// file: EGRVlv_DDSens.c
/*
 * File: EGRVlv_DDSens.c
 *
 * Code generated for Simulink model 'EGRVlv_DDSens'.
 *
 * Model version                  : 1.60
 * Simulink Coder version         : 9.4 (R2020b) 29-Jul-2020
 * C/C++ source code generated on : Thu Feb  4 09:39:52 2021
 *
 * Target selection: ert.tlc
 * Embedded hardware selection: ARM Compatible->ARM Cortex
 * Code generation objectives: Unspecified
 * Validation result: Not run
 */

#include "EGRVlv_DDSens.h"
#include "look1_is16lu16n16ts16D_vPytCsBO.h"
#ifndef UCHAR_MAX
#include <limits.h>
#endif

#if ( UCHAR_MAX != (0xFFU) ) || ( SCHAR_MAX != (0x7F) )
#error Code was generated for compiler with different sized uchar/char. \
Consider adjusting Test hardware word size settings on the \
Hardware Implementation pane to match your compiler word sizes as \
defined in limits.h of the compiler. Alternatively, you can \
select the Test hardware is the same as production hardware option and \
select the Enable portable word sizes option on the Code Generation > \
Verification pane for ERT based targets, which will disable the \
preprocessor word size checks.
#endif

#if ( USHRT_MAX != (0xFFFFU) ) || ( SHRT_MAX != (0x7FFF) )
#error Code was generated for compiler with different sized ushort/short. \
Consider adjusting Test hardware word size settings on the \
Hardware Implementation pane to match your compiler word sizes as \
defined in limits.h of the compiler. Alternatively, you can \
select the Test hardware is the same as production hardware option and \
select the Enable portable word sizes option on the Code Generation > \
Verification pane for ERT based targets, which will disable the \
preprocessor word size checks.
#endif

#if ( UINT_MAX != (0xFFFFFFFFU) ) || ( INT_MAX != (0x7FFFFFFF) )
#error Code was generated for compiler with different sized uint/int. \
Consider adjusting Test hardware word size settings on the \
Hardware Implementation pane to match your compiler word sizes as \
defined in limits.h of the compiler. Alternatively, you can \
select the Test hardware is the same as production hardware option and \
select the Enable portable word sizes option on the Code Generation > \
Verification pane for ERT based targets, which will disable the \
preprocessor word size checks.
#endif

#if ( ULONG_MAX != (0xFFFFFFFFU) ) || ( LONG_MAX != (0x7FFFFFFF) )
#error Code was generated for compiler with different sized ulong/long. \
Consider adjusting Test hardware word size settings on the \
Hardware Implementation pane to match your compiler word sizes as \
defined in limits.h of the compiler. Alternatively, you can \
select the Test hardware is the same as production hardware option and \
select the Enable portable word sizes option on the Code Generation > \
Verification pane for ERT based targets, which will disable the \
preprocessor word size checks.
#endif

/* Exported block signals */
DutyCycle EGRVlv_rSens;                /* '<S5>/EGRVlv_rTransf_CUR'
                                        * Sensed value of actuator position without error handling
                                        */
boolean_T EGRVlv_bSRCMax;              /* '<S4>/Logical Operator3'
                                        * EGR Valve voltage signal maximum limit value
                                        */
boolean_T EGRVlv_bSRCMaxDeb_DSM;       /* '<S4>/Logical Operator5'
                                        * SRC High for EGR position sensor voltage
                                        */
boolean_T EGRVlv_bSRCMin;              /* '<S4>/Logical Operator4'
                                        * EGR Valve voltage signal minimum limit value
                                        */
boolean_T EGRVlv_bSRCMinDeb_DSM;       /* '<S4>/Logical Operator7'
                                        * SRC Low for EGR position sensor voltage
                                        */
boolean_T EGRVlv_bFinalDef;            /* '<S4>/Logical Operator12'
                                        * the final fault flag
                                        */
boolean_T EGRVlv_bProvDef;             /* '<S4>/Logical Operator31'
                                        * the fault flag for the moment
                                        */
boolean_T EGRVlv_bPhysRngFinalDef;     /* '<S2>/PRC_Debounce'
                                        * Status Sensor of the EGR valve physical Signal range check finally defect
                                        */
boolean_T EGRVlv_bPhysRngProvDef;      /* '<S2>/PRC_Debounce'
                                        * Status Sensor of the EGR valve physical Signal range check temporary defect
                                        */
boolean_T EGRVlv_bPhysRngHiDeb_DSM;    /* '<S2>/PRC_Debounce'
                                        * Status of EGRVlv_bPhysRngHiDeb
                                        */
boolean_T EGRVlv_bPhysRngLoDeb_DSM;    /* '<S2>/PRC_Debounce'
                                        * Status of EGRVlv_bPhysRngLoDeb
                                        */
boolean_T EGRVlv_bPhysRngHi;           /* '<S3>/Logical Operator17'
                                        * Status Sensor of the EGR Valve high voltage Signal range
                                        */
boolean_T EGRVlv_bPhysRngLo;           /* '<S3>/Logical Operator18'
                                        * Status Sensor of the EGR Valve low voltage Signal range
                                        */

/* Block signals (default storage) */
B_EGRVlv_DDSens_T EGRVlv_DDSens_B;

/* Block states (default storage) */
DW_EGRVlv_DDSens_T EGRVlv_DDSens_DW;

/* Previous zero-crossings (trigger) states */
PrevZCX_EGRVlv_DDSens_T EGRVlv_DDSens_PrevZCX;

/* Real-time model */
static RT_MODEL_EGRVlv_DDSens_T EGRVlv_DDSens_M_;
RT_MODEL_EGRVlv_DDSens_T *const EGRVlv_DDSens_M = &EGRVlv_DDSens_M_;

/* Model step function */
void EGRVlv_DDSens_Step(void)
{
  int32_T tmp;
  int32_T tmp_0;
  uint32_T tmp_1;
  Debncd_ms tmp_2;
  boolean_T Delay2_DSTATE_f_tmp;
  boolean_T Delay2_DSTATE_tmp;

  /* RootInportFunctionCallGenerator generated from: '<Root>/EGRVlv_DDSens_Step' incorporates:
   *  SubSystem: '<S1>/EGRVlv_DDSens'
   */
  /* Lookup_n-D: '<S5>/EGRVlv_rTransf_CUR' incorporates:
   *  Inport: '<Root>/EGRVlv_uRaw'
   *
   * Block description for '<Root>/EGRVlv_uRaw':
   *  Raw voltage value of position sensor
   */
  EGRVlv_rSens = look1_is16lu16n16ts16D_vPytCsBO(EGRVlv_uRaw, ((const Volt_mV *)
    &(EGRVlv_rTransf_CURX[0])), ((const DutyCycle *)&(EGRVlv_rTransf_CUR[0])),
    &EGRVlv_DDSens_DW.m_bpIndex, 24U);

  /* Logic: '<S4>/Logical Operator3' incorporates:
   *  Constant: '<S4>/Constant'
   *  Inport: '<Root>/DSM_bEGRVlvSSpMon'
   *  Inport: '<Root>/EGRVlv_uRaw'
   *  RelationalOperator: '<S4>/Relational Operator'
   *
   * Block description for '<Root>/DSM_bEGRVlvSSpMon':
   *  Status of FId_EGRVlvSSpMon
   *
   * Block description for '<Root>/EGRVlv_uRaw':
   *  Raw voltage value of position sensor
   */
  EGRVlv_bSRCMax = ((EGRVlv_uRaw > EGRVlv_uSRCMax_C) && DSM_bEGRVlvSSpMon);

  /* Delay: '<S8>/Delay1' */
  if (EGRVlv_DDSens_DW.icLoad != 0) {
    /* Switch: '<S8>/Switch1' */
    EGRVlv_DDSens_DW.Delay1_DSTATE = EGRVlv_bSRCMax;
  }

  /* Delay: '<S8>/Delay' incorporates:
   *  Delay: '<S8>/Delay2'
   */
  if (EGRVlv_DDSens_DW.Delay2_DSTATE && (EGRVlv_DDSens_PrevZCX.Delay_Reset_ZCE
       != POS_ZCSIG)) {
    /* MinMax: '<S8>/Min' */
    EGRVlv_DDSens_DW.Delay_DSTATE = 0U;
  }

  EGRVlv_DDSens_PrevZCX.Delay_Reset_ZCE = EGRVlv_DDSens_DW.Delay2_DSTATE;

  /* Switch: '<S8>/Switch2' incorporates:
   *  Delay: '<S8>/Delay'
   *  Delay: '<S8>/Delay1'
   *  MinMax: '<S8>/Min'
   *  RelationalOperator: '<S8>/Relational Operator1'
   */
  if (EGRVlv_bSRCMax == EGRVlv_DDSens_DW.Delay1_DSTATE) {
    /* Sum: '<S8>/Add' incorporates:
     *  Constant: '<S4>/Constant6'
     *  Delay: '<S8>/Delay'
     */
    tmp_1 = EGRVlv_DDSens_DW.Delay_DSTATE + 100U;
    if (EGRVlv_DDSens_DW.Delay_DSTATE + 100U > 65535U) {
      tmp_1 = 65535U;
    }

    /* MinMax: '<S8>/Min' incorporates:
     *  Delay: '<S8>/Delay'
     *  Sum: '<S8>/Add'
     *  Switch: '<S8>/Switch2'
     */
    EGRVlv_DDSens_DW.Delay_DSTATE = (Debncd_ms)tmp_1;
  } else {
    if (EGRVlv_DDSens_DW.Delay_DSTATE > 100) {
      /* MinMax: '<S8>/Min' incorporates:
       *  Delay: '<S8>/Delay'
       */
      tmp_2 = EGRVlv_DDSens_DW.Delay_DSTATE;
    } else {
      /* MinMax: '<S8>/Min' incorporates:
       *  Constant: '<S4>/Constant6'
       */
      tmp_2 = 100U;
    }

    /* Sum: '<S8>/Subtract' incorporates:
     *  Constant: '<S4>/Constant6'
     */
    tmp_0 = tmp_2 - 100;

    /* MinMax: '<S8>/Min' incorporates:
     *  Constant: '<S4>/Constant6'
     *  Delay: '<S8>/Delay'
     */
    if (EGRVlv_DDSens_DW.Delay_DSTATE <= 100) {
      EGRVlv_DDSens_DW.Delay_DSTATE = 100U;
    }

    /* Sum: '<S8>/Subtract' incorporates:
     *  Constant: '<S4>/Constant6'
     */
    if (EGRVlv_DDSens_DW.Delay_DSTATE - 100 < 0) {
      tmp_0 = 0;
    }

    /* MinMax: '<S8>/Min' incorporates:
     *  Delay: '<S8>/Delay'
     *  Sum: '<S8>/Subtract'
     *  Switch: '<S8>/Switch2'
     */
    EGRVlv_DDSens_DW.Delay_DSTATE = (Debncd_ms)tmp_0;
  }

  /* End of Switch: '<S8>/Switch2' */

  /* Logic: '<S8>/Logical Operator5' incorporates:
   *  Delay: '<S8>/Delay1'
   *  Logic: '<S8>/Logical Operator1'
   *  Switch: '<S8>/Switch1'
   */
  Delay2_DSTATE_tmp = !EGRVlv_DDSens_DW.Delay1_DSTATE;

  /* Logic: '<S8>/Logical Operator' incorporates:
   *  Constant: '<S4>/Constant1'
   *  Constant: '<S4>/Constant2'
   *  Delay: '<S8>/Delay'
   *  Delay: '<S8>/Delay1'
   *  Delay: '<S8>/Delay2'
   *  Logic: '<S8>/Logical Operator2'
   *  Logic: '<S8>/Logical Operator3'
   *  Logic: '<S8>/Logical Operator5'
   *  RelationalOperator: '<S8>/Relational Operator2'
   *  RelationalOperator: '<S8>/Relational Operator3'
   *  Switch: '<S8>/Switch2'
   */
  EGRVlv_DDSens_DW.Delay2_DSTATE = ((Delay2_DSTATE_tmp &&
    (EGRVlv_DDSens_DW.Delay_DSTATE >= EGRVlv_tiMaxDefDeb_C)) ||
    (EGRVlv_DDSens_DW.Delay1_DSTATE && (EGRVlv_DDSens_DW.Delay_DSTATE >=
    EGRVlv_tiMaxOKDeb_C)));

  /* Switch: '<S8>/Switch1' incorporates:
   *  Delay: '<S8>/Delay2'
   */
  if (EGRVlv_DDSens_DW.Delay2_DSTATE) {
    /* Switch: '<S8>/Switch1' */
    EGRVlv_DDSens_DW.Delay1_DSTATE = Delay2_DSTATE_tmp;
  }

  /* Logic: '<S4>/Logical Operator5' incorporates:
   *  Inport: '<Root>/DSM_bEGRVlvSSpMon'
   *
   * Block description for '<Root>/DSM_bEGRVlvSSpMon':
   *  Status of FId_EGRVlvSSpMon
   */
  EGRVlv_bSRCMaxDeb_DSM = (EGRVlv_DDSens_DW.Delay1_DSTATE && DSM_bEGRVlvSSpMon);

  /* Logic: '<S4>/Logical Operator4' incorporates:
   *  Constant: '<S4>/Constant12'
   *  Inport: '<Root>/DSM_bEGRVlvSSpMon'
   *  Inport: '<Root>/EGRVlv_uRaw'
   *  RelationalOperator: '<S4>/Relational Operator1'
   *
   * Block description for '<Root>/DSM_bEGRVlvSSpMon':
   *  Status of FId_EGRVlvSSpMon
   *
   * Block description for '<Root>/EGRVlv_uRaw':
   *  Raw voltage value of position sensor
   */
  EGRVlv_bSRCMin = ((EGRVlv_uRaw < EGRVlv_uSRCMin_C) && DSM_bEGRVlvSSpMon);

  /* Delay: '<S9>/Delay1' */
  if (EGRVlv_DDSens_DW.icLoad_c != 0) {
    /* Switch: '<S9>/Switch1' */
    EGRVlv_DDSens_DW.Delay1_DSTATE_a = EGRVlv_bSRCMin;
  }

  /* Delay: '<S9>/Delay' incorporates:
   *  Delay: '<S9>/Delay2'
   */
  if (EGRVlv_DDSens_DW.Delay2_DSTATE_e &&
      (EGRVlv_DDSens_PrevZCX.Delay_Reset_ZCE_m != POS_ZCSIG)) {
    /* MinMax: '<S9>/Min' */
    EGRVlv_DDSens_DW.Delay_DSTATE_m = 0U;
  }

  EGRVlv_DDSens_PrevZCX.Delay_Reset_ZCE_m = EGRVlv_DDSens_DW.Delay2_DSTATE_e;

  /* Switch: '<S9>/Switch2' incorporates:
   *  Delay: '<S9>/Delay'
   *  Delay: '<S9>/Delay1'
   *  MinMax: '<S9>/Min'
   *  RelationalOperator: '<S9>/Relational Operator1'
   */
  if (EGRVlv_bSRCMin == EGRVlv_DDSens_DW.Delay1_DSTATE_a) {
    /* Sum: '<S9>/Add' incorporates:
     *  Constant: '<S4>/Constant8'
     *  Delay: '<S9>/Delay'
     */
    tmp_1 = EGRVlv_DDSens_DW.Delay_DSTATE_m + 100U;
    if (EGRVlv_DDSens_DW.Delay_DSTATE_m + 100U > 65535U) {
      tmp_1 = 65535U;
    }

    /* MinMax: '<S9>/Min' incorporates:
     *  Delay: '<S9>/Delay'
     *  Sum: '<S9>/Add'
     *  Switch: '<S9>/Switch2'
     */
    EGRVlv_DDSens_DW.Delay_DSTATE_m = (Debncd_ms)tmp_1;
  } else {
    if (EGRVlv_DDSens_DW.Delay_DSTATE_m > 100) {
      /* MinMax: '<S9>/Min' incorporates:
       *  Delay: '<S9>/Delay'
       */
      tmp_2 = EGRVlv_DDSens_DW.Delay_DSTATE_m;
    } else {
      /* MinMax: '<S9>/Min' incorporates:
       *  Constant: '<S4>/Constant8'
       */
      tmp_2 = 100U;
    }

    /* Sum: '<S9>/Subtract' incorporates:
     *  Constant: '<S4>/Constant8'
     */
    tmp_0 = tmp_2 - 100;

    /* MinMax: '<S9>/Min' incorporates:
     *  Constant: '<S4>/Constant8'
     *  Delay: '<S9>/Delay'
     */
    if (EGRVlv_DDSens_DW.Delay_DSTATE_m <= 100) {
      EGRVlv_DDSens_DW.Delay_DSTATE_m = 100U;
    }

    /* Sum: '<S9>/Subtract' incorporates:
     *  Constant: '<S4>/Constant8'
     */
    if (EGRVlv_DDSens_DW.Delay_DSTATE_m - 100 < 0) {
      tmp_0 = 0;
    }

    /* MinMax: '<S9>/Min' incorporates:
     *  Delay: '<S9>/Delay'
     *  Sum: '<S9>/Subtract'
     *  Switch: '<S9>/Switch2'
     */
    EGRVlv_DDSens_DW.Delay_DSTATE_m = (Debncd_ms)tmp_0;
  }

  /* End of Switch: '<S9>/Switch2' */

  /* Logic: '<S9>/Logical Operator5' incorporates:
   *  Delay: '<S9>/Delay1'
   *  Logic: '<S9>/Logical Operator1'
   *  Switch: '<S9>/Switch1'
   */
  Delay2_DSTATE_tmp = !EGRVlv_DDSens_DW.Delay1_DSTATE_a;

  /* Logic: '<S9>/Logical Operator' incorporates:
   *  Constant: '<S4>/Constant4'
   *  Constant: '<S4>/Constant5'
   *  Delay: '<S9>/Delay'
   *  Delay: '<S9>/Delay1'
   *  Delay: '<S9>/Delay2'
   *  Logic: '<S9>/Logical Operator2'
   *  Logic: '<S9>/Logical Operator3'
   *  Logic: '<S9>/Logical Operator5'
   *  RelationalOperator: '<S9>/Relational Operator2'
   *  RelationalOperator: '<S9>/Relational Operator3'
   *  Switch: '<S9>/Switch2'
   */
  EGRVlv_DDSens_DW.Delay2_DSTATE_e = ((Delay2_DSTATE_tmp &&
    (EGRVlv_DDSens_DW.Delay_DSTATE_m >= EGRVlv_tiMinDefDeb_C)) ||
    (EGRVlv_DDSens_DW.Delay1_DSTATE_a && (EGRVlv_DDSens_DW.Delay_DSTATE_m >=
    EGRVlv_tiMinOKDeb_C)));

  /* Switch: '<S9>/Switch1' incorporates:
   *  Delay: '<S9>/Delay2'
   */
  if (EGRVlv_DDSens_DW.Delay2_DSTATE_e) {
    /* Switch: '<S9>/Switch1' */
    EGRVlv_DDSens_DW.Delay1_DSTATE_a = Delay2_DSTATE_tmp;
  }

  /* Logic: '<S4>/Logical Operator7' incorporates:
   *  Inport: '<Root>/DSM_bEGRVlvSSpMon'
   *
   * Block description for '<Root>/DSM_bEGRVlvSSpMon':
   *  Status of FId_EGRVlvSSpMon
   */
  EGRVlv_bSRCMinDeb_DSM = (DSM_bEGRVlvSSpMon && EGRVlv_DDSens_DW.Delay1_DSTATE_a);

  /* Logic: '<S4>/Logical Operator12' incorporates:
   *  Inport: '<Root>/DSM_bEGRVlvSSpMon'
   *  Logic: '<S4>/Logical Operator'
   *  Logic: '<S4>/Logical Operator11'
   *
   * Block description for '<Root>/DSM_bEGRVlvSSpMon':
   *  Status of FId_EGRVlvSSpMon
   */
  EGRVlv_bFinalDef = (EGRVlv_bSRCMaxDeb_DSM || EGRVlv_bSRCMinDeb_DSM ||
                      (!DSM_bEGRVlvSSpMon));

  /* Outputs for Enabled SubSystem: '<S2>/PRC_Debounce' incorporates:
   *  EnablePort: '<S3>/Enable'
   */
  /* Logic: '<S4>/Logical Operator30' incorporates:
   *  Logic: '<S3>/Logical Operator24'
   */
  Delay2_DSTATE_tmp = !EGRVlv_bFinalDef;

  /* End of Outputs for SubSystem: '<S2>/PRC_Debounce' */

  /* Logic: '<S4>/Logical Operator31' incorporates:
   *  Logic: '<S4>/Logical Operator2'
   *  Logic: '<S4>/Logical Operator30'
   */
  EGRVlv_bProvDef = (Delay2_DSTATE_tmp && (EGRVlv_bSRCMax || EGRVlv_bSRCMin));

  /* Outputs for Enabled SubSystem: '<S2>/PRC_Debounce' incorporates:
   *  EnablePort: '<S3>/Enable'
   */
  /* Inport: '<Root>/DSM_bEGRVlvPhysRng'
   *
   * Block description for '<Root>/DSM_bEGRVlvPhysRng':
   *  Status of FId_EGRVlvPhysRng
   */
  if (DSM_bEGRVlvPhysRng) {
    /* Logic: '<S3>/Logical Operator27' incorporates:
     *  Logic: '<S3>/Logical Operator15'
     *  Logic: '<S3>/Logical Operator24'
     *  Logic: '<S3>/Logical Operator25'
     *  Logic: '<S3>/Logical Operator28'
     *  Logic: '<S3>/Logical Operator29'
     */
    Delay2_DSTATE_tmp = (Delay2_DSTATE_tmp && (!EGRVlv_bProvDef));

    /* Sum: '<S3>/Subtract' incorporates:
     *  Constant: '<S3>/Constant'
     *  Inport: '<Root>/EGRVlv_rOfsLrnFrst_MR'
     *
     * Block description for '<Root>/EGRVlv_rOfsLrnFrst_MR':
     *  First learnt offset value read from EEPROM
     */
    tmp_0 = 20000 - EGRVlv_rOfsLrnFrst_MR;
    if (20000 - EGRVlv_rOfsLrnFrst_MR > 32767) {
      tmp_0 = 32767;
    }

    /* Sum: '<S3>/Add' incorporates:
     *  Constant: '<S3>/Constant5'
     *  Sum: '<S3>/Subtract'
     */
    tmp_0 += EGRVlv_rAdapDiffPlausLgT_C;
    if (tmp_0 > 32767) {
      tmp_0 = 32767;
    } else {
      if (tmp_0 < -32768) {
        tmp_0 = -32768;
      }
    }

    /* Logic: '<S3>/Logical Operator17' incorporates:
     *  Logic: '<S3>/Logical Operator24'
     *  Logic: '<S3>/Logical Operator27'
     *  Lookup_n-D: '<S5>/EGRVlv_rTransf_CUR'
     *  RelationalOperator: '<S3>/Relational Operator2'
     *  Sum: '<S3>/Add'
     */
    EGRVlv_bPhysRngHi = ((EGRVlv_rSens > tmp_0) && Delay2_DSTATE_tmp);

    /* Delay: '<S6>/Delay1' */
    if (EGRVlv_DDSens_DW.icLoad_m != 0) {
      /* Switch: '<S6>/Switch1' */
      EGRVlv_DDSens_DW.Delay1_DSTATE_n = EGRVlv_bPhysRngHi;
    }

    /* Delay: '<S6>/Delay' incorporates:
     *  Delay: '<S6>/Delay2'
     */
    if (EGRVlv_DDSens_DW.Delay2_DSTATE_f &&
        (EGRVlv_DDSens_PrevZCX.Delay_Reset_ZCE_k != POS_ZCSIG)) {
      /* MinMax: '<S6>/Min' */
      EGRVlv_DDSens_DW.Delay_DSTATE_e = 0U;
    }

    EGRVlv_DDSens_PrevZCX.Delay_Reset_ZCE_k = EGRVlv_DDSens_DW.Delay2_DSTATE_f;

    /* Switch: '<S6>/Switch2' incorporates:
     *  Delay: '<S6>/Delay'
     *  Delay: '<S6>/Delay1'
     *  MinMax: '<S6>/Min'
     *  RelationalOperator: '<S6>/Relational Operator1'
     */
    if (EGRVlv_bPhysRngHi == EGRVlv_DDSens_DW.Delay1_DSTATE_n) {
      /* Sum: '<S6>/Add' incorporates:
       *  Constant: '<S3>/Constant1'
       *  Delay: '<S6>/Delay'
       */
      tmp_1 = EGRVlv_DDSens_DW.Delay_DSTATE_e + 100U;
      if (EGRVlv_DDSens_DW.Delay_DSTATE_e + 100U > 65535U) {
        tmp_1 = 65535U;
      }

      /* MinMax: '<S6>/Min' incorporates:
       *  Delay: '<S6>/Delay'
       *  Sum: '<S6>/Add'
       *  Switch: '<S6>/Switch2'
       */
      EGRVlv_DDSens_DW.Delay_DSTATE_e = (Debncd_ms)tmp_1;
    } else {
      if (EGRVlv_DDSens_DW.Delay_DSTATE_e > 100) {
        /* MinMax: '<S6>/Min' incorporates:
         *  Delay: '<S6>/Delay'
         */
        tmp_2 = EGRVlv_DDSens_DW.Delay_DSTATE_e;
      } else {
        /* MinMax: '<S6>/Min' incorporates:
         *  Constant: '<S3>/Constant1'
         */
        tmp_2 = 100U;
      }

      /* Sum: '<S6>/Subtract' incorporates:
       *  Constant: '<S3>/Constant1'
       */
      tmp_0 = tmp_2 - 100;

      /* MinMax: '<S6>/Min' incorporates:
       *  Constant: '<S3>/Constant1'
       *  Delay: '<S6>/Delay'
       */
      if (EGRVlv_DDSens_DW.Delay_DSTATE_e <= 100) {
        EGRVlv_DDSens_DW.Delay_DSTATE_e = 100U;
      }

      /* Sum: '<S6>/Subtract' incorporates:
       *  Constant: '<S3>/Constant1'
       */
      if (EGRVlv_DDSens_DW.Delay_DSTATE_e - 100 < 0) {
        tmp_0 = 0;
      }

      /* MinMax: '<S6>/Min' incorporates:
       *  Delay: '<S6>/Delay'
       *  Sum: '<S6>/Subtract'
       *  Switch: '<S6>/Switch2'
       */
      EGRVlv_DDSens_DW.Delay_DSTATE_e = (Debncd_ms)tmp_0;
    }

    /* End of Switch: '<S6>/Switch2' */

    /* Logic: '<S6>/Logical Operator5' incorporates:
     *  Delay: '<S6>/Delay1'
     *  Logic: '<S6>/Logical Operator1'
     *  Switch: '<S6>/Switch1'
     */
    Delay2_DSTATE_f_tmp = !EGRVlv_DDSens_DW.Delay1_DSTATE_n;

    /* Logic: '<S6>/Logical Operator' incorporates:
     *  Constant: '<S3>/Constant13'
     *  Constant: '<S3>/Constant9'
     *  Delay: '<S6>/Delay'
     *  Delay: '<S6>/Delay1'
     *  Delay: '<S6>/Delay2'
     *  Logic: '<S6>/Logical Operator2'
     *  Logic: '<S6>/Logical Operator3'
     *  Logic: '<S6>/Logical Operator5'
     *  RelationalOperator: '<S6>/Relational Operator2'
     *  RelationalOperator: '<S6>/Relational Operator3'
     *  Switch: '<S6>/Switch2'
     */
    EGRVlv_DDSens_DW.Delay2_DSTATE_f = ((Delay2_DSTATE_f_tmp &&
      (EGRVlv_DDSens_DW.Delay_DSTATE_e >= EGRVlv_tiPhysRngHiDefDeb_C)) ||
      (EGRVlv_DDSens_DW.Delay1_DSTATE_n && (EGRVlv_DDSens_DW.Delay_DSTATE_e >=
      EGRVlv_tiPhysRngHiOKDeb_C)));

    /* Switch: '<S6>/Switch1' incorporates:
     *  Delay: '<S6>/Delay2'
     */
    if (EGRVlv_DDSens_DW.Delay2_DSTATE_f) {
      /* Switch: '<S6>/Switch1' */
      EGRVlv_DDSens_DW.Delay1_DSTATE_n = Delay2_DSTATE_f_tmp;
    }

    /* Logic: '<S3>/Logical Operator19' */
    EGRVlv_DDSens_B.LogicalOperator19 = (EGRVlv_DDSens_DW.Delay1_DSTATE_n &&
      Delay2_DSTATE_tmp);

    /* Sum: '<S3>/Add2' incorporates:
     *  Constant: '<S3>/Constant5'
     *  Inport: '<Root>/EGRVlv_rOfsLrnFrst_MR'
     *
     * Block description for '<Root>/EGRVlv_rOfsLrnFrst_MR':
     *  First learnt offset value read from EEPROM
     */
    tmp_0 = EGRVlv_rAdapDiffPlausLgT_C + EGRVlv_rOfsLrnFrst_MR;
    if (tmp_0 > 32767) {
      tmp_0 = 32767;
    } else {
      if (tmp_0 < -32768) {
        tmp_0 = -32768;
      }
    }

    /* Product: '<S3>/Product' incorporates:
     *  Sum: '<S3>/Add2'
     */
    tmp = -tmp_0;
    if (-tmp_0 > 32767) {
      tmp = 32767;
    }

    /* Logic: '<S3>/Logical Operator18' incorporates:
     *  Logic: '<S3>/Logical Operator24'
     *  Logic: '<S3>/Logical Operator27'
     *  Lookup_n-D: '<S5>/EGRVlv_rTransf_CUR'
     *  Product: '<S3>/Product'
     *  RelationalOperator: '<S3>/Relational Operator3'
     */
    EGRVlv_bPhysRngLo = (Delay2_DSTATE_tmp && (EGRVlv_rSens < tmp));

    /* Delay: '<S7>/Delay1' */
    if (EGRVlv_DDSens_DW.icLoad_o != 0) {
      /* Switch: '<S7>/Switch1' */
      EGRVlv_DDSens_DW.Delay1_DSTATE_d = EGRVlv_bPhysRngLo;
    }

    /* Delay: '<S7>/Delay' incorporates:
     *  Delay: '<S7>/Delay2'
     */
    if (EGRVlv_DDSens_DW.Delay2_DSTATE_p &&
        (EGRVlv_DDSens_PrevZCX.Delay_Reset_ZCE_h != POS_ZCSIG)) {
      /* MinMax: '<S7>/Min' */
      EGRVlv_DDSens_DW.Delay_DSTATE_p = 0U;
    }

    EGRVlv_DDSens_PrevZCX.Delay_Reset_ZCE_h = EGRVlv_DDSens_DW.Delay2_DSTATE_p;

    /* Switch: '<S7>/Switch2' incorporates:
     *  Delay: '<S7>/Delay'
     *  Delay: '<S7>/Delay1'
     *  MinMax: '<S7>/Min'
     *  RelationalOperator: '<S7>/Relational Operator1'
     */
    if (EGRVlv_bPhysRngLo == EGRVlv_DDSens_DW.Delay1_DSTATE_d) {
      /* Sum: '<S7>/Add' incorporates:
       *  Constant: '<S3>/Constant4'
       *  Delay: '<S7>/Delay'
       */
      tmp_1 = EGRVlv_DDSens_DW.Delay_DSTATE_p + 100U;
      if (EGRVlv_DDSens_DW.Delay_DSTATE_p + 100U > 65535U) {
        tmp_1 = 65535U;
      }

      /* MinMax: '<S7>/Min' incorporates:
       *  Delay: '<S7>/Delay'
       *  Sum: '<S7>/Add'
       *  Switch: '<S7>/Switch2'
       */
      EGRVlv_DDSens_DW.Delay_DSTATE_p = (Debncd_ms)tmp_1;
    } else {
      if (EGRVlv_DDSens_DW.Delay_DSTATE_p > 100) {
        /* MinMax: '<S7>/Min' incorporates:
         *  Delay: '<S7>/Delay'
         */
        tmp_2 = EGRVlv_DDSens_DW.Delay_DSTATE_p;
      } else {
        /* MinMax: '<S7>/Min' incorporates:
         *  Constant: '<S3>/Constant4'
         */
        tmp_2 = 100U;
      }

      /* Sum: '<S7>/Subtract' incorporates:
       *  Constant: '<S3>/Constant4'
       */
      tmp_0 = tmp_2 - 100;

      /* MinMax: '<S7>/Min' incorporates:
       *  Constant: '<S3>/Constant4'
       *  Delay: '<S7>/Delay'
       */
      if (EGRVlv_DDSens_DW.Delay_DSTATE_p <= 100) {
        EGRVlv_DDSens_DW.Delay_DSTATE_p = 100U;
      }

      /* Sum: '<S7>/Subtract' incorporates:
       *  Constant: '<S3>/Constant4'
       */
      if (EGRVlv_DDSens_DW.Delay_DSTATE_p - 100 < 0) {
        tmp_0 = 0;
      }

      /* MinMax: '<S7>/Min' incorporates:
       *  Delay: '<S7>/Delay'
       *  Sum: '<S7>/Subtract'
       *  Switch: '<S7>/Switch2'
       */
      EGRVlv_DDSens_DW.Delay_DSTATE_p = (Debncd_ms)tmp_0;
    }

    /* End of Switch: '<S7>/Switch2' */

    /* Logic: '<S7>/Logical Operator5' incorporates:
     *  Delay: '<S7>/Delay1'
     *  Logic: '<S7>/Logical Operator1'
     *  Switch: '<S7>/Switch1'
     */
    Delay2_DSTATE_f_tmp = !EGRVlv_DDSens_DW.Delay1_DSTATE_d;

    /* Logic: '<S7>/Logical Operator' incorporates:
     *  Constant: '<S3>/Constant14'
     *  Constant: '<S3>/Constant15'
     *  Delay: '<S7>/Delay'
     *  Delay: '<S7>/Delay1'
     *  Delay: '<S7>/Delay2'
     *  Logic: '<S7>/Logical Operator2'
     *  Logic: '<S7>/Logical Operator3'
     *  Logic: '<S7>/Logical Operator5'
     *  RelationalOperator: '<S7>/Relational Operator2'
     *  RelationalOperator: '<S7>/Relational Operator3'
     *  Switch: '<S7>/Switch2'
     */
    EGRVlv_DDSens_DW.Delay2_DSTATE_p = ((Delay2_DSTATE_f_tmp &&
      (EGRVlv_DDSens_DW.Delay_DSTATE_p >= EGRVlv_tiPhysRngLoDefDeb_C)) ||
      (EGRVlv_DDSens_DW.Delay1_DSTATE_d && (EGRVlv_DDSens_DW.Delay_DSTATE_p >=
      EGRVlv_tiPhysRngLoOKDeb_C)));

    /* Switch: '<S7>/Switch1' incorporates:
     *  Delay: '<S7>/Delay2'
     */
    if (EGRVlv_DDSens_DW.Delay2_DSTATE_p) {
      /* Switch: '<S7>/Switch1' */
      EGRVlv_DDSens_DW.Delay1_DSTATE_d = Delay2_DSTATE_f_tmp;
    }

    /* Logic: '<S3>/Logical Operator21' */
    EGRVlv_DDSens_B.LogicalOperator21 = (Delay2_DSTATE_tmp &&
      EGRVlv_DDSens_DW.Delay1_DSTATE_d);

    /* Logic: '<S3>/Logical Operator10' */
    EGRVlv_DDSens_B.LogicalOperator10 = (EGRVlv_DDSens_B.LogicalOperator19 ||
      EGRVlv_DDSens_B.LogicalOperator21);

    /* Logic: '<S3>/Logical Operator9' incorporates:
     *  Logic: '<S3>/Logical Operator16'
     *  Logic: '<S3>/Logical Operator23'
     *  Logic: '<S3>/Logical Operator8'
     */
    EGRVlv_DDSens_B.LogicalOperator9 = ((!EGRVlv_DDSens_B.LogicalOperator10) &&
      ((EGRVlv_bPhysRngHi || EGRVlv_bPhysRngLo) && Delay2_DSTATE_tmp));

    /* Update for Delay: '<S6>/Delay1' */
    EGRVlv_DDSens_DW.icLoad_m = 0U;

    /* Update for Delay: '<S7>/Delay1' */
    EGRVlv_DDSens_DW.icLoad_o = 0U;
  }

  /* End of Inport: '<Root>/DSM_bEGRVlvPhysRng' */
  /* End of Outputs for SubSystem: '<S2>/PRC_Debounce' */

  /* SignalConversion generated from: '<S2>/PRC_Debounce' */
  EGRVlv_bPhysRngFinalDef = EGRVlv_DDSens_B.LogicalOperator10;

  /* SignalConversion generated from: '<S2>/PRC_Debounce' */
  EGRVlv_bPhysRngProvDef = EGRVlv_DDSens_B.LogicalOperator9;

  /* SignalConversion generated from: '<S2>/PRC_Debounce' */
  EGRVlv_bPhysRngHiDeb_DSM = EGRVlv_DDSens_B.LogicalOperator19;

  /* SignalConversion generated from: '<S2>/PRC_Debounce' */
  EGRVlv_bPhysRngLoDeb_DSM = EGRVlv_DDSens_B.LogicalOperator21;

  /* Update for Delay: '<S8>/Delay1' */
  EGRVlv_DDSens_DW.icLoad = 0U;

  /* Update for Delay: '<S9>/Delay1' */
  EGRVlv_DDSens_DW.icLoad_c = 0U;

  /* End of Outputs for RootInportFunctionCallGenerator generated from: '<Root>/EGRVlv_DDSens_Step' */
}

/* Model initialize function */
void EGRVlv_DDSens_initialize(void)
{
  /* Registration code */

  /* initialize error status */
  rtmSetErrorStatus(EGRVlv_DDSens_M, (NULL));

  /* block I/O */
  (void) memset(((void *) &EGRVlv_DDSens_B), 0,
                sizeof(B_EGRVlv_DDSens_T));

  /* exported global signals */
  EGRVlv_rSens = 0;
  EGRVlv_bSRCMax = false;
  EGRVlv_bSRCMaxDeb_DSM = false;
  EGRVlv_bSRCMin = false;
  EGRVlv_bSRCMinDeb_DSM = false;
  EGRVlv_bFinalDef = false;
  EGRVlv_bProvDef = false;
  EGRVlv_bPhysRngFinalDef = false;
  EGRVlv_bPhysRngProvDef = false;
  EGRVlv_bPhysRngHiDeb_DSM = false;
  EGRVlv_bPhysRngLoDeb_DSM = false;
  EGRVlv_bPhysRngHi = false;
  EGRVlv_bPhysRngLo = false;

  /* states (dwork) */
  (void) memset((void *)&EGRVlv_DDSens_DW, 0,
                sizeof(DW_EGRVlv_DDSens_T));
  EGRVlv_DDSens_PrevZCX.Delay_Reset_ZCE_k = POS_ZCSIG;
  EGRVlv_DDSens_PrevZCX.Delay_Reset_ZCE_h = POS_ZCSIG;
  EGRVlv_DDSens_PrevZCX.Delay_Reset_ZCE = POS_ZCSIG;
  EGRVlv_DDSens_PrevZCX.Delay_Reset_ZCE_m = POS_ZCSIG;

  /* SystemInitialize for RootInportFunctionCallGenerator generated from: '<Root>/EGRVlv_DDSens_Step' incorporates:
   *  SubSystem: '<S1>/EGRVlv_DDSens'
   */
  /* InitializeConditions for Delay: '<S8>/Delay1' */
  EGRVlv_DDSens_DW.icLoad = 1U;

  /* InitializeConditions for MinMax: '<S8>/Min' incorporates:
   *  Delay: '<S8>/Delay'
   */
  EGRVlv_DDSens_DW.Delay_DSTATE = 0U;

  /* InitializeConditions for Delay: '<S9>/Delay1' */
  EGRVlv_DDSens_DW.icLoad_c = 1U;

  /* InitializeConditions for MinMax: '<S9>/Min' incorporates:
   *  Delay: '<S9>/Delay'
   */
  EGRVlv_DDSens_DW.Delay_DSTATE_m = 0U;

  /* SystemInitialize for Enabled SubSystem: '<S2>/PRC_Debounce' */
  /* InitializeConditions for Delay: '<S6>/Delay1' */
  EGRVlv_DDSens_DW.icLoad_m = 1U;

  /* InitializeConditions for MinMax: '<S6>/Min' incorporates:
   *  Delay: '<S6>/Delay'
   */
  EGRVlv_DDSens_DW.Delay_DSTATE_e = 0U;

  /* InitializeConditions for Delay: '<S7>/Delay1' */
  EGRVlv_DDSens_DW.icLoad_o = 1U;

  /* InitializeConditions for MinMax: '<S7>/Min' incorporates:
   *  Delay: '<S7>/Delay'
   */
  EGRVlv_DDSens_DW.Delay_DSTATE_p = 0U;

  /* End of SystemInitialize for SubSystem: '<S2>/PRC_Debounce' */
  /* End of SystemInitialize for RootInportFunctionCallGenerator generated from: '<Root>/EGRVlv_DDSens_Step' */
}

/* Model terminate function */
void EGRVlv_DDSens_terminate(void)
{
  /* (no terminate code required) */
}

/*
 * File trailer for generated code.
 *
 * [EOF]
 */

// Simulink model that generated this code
simulink model "EGRVlv_DDSens"  (R2018a)
settings: configuration reference "cs_ert" (kept outside this file)
model workspace (MAT data in the model file):
  EGRVlv_DDSens_DT = 10
values from neighbouring files (symbols this model uses):
  EGRVlv_rAdapDiffPlausLgT_C = 20.0    [EGRVlv_DDSens.sldd]
  EGRVlv_rTransf_CUR : value not decoded    [EGRVlv_DDSens.sldd]
  EGRVlv_rTransf_CURX : value not decoded    [EGRVlv_DDSens.sldd]
  EGRVlv_tiMaxDefDeb_C = 200.0    [EGRVlv_DDSens.sldd]
  EGRVlv_tiMaxOKDeb_C = 200.0    [EGRVlv_DDSens.sldd]
  EGRVlv_tiMinDefDeb_C = 200.0    [EGRVlv_DDSens.sldd]
  EGRVlv_tiMinOKDeb_C = 200.0    [EGRVlv_DDSens.sldd]
  EGRVlv_tiPhysRngHiDefDeb_C = 200.0    [EGRVlv_DDSens.sldd]
  EGRVlv_tiPhysRngHiOKDeb_C = 200.0    [EGRVlv_DDSens.sldd]
  EGRVlv_tiPhysRngLoDefDeb_C = 200.0    [EGRVlv_DDSens.sldd]
  EGRVlv_tiPhysRngLoOKDeb_C = 200.0    [EGRVlv_DDSens.sldd]
  EGRVlv_uSRCMax_C = 4800.0    [EGRVlv_DDSens.sldd]
  EGRVlv_uSRCMin_C = 200.0    [EGRVlv_DDSens.sldd]
undefined symbols (not defined in the file or in its folder): CEngDsT_tTransf_CURX
libraries: sllib x4

== system EGRVlv_DDSens ==
  EGRVlv_DDSens_Step : Inport  OutputFunctionCall=on
  EGRVlv_uRaw : Inport  Description=Raw voltage value of position sensor  Port=2  OutMin=0  OutMax=5000  OutDataTypeStr=Volt_mV  Unit=mv  PortDimensions=[1 1]
  DSM_bEGRVlvSSpMon : Inport  Description=Status of FId_EGRVlvSSpMon  Port=3  OutMin=0  OutMax=1  OutDataTypeStr=boolean  PortDimensions=[1 1]
  EGRVlv_rOfsLrnFrst_MR : Inport  Description=First learnt offset value read from EEPROM  Port=4  OutMin=-100  OutMax=100  OutDataTypeStr=DutyCycle  Unit=%  PortDimensions=[1 1]
  DSM_bEGRVlvPhysRng : Inport  Description=Status of FId_EGRVlvPhysRng  Port=5  OutMin=0  OutMax=1  OutDataTypeStr=boolean  PortDimensions=[1 1]
  Overview : Subsystem
  EGRVlv_rSens : Outport  Description=Sensed value of actuator position without error handling  OutMin=-100  OutMax=100  OutDataTypeStr=DutyCycle  Unit=%  PortDimensions=[1 1]
  EGRVlv_bFinalDef : Outport  Description=the final fault flag  Port=2  OutMin=0  OutMax=1  OutDataTypeStr=boolean  PortDimensions=[1 1]
  EGRVlv_bProvDef : Outport  Description=the fault flag for the moment  Port=3  OutMin=0  OutMax=1  OutDataTypeStr=boolean  PortDimensions=[1 1]
  EGRVlv_bSRCMaxDeb_DSM : Outport  Description=SRC High for EGR position sensor voltage  Port=4  OutMin=0  OutMax=1  OutDataTypeStr=boolean  PortDimensions=[1 1]
  EGRVlv_bSRCMinDeb_DSM : Outport  Description=SRC Low for EGR position sensor voltage  Port=5  OutMin=0  OutMax=1  OutDataTypeStr=boolean  PortDimensions=[1 1]
  EGRVlv_bPhysRngHiDeb_DSM : Outport  Description=Status of EGRVlv_bPhysRngHiDeb  Port=6  OutMin=0  OutMax=1  OutDataTypeStr=boolean  PortDimensions=[1 1]
  EGRVlv_bPhysRngLoDeb_DSM : Outport  Description=Status of EGRVlv_bPhysRngLoDeb  Port=7  OutMin=0  OutMax=1  OutDataTypeStr=boolean  PortDimensions=[1 1]
  EGRVlv_bPhysRngFinalDef : Outport  Description=Status Sensor of the EGR valve physical Signal range check finally defect  Port=8  OutMin=0  OutMax=1  OutDataTypeStr=boolean  PortDimensions=[1 1]
  EGRVlv_bPhysRngProvDef : Outport  Description=Status Sensor of the EGR valve physical Signal range check temporary defect  Port=9  OutMin=0  OutMax=1  OutDataTypeStr=boolean  PortDimensions=[1 1]
  wires:
  EGRVlv_DDSens_Step/1 -> Overview/1(EGRVlv_DDSens_Step)
  EGRVlv_uRaw/1 -> Overview/2(EGRVlv_uRaw)
  DSM_bEGRVlvSSpMon/1 -> Overview/3(DSM_bEGRVlvSSpMon)
  EGRVlv_rOfsLrnFrst_MR/1 -> Overview/4(EGRVlv_rOfsLrnFrst_MR)
  DSM_bEGRVlvPhysRng/1 -> Overview/5(DSM_bEGRVlvPhysRng)
  Overview/1(EGRVlv_rSens) -> EGRVlv_rSens/1
  Overview/2(EGRVlv_bFinalDef) -> EGRVlv_bFinalDef/1
  Overview/3(EGRVlv_bProvDef) -> EGRVlv_bProvDef/1
  Overview/4(EGRVlv_bSRCMaxDeb_DSM) -> EGRVlv_bSRCMaxDeb_DSM/1
  Overview/5(EGRVlv_bSRCMinDeb_DSM) -> EGRVlv_bSRCMinDeb_DSM/1
  Overview/6(EGRVlv_bPhysRngHiDeb_DSM) -> EGRVlv_bPhysRngHiDeb_DSM/1
  Overview/7(EGRVlv_bPhysRngLoDeb_DSM) -> EGRVlv_bPhysRngLoDeb_DSM/1
  Overview/8(EGRVlv_bPhysRngFinalDef) -> EGRVlv_bPhysRngFinalDef/1
  Overview/9(EGRVlv_bPhysRngProvDef) -> EGRVlv_bPhysRngProvDef/1

== system EGRVlv_DDSens/Overview ==
  EGRVlv_DDSens_Step : Inport
  EGRVlv_uRaw : Inport  Port=2
  DSM_bEGRVlvSSpMon : Inport  Port=3
  EGRVlv_rOfsLrnFrst_MR : Inport  Port=4
  DSM_bEGRVlvPhysRng : Inport  Port=5
  EGRVlv_DDSens : Subsystem
  EGRVlv_rSens : Outport
  EGRVlv_bFinalDef : Outport  Port=2
  EGRVlv_bProvDef : Outport  Port=3
  EGRVlv_bSRCMaxDeb_DSM : Outport  Port=4
  EGRVlv_bSRCMinDeb_DSM : Outport  Port=5
  EGRVlv_bPhysRngHiDeb_DSM : Outport  Port=6
  EGRVlv_bPhysRngLoDeb_DSM : Outport  Port=7
  EGRVlv_bPhysRngFinalDef : Outport  Port=8
  EGRVlv_bPhysRngProvDef : Outport  Port=9
  wires:
  EGRVlv_uRaw/1 -> EGRVlv_DDSens/1(EGRVlv_uRaw)
  DSM_bEGRVlvSSpMon/1 -> EGRVlv_DDSens/2(DSM_bEGRVlvSSpMon)
  EGRVlv_rOfsLrnFrst_MR/1 -> EGRVlv_DDSens/3(EGRVlv_rOfsLrnFrst_MR)
  DSM_bEGRVlvPhysRng/1 -> EGRVlv_DDSens/4(DSM_bEGRVlvPhysRng)
  EGRVlv_DDSens/1(EGRVlv_rSens) -> EGRVlv_rSens/1
  EGRVlv_DDSens/2(EGRVlv_bFinalDef) -> EGRVlv_bFinalDef/1
  EGRVlv_DDSens/3(EGRVlv_bProvDef) -> EGRVlv_bProvDef/1
  EGRVlv_DDSens/4(EGRVlv_bSRCMaxDeb_DSM) -> EGRVlv_bSRCMaxDeb_DSM/1
  EGRVlv_DDSens/5(EGRVlv_bSRCMinDeb_DSM) -> EGRVlv_bSRCMinDeb_DSM/1
  EGRVlv_DDSens/6(EGRVlv_bPhysRngHiDeb_DSM) -> EGRVlv_bPhysRngHiDeb_DSM/1
  EGRVlv_DDSens/7(EGRVlv_bPhysRngLoDeb_DSM) -> EGRVlv_bPhysRngLoDeb_DSM/1
  EGRVlv_DDSens/8(EGRVlv_bPhysRngFinalDef) -> EGRVlv_bPhysRngFinalDef/1
  EGRVlv_DDSens/9(EGRVlv_bPhysRngProvDef) -> EGRVlv_bPhysRngProvDef/1
  EGRVlv_DDSens_Step/1 -> EGRVlv_DDSens/Trigger

== system EGRVlv_DDSens/Overview/EGRVlv_DDSens ==
  EGRVlv_uRaw : Inport  Tag=mv
  DSM_bEGRVlvSSpMon : Inport  Port=2
  EGRVlv_rOfsLrnFrst_MR : Inport  Port=3
  DSM_bEGRVlvPhysRng : Inport  Port=4
  Trigger : TriggerPort  TriggerType=function-call  VariantControl=Variant  PortDimensions=1
  PRC_Debounce : Subsystem
  SRC_Debounce : Subsystem
  U2R_Cnv : Subsystem
  EGRVlv_rSens : Outport  Tag=%
  EGRVlv_bFinalDef : Outport  Port=2
  EGRVlv_bProvDef : Outport  Port=3
  EGRVlv_bSRCMaxDeb_DSM : Outport  Port=4
  EGRVlv_bSRCMinDeb_DSM : Outport  Port=5
  EGRVlv_bPhysRngHiDeb_DSM : Outport  Port=6
  EGRVlv_bPhysRngLoDeb_DSM : Outport  Port=7
  EGRVlv_bPhysRngFinalDef : Outport  Port=8
  EGRVlv_bPhysRngProvDef : Outport  Port=9
  wires:
  SRC_Debounce/2(EGRVlv_bFinalDef) -> EGRVlv_bFinalDef/1, [EGRVlv_bFinalDef]  "EGRVlv_bFinalDef"
  EGRVlv_uRaw/1 -> SRC_Debounce/1(EGRVlv_uRaw), U2R_Cnv/1(EGRVlv_uRaw)
  SRC_Debounce/4(EGRVlv_bProvDef) -> EGRVlv_bProvDef/1, [EGRVlv_bProvDef]  "EGRVlv_bProvDef"
  U2R_Cnv/1(EGRVlv_rSens) -> EGRVlv_rSens/1, PRC_Debounce/2(EGRVlv_rSens)  "EGRVlv_rSens"
  EGRVlv_rOfsLrnFrst_MR/1 -> PRC_Debounce/1(EGRVlv_rOfsLrnFrst_MR)
  [EGRVlv_bProvDef] -> PRC_Debounce/3(EGRVlv_bProvDef)
  [EGRVlv_bFinalDef] -> PRC_Debounce/4(EGRVlv_bFinalDef)
  DSM_bEGRVlvSSpMon/1 -> SRC_Debounce/2(DSM_bEGRVlvSSpMon)
  PRC_Debounce/1(EGRVlv_bPhysRngFinalDef) -> EGRVlv_bPhysRngFinalDef/1  "EGRVlv_bPhysRngFinalDef"
  PRC_Debounce/2(EGRVlv_bPhysRngProvDef) -> EGRVlv_bPhysRngProvDef/1  "EGRVlv_bPhysRngProvDef"
  PRC_Debounce/3(EGRVlv_bPhysRngHiDeb_DSM) -> EGRVlv_bPhysRngHiDeb_DSM/1  "EGRVlv_bPhysRngHiDeb_DSM"
  PRC_Debounce/4(EGRVlv_bPhysRngLoDeb_DSM) -> EGRVlv_bPhysRngLoDeb_DSM/1  "EGRVlv_bPhysRngLoDeb_DSM"
  SRC_Debounce/1(EGRVlv_bSRCMaxDeb_DSM) -> EGRVlv_bSRCMaxDeb_DSM/1  "EGRVlv_bSRCMaxDeb_DSM"
  SRC_Debounce/3(EGRVlv_bSRCMinDeb_DSM) -> EGRVlv_bSRCMinDeb_DSM/1  "EGRVlv_bSRCMinDeb_DSM"
  DSM_bEGRVlvPhysRng/1 -> PRC_Debounce/Enable

== system EGRVlv_DDSens/Overview/EGRVlv_DDSens/PRC_Debounce ==
  EGRVlv_rOfsLrnFrst_MR : Inport
  EGRVlv_rSens : Inport  Port=2
  EGRVlv_bProvDef : Inport  Port=3
  EGRVlv_bFinalDef : Inport  Port=4
  Enable : EnablePort
  Add : Sum  SaturateOnIntegerOverflow=on
  Add1 : Sum  SaturateOnIntegerOverflow=on  InputSameDT=on
  Add2 : Sum  SaturateOnIntegerOverflow=on
  Constant : Constant  Value=100  OutDataTypeStr=Inherit: Inherit via back propagation
  Constant1 : Constant  Value=EGRVlv_DDSens_DT  OutDataTypeStr=Inherit: Inherit via back propagation
  Constant13 : Constant  Value=EGRVlv_tiPhysRngHiDefDeb_C
  Constant14 : Constant  Value=EGRVlv_tiPhysRngLoDefDeb_C
  Constant15 : Constant  Value=EGRVlv_tiPhysRngLoOKDeb_C
  Constant4 : Constant  Value=EGRVlv_DDSens_DT  OutDataTypeStr=Inherit: Inherit via back propagation
  Constant5 : Constant  Value=EGRVlv_rAdapDiffPlausLgT_C
  Constant6 : Constant  Value=0  OutDataTypeStr=Inherit: Inherit via back propagation
  Constant7 : Constant  Value=-1  OutDataTypeStr=int8
  Constant9 : Constant  Value=EGRVlv_tiPhysRngHiOKDeb_C
  Debounce_DT : sllib/Debounce_DT
  Debounce_DT1 : sllib/Debounce_DT
  Logical Operator10 : Logic  Operator=OR  AllPortsSameDT=off  OutDataTypeStr=boolean
  Logical Operator{8,15,27..28} (4 alike) : Logic  Operator=NOT  AllPortsSameDT=off  OutDataTypeStr=boolean
  Logical Operator16 : Logic  Operator=OR  AllPortsSameDT=off  OutDataTypeStr=boolean
  Logical Operator{9,17..19,21,23} (6 alike) : Logic  AllPortsSameDT=off  OutDataTypeStr=boolean
  Logical Operator24 : Logic  Operator=OR  OutDataTypeStr=boolean
  Logical Operator25 : Logic  Operator=OR  OutDataTypeStr=boolean
  Logical Operator29 : Logic  Operator=OR  OutDataTypeStr=boolean
  Product : Product  OutDataTypeStr=Inherit: Inherit via back propagation  SaturateOnIntegerOverflow=on
  Relational Operator2 : RelationalOperator  Operator=>  OutDataTypeStr=boolean  RndMeth=Nearest  InputSameDT=on
  Relational Operator3 : RelationalOperator  Operator=<  OutDataTypeStr=boolean  RndMeth=Nearest  InputSameDT=on
  Subtract : Sum  Inputs=+-  SaturateOnIntegerOverflow=on
  EGRVlv_bPhysRngFinalDef : Outport  Tag=-  InitialOutput=0
  EGRVlv_bPhysRngProvDef : Outport  Tag=-  Port=2  InitialOutput=0
  EGRVlv_bPhysRngHiDeb_DSM : Outport  Tag=-  Port=3  InitialOutput=0
  EGRVlv_bPhysRngLoDeb_DSM : Outport  Tag=-  Port=4  InitialOutput=0
  wires:
  EGRVlv_rSens/1 -> Relational Operator2/1, Relational Operator3/1
  Constant15/1 -> Debounce_DT1/3
  Constant13/1 -> Debounce_DT/2
  Constant9/1 -> Debounce_DT/3
  Constant14/1 -> Debounce_DT1/2
  Constant1/1 -> Debounce_DT/4
  Constant4/1 -> Debounce_DT1/4
  Add/1 -> Relational Operator2/2
  Logical Operator17/1 -> Debounce_DT/1, [bPhysRngHi]  "EGRVlv_bPhysRngHi"
  Add1/1 -> Relational Operator3/2
  Logical Operator18/1 -> Debounce_DT1/1, [bPhysRngLo]  "EGRVlv_bPhysRngLo"
  Logical Operator19/1 -> Logical Operator10/1, EGRVlv_bPhysRngHiDeb_DSM/1
  Logical Operator21/1 -> EGRVlv_bPhysRngLoDeb_DSM/1, Logical Operator10/2
  [bPhysRngHi] -> Logical Operator16/1
  [bPhysRngLo] -> Logical Operator16/2
  Relational Operator2/1 -> Logical Operator17/1
  Logical Operator24/1 -> Logical Operator27/1
  Logical Operator25/1 -> Logical Operator28/1
  Logical Operator16/1 -> Logical Operator23/1
  Logical Operator15/1 -> Logical Operator23/2
  Relational Operator3/1 -> Logical Operator18/2
  EGRVlv_bFinalDef/1 -> [bFinalDef], Logical Operator24/1
  EGRVlv_bProvDef/1 -> Logical Operator24/2, [bProvDef]
  [bFinalDef] -> Logical Operator25/1
  [bProvDef] -> Logical Operator25/2
  Logical Operator27/1 -> Logical Operator17/2, Logical Operator18/1
  Logical Operator28/1 -> Logical Operator21/1, Logical Operator19/2
  [bFinalDef] -> Logical Operator29/1
  [bProvDef] -> Logical Operator29/2
  Logical Operator29/1 -> Logical Operator15/1
  Logical Operator10/1 -> EGRVlv_bPhysRngFinalDef/1, Logical Operator8/1
  Logical Operator8/1 -> Logical Operator9/1
  Logical Operator9/1 -> EGRVlv_bPhysRngProvDef/1
  Logical Operator23/1 -> Logical Operator9/2
  Constant/1 -> Subtract/1
  EGRVlv_rOfsLrnFrst_MR/1 -> Add2/2, Subtract/2
  Subtract/1 -> Add/1
  Constant5/1 -> Add/2, Add2/1
  Constant7/1 -> Product/2
  Constant6/1 -> Add1/2
  Product/1 -> Add1/1
  Add2/1 -> Product/1
  Debounce_DT/1 -> Logical Operator19/1
  Debounce_DT1/1 -> Logical Operator21/2

== system EGRVlv_DDSens/Overview/EGRVlv_DDSens/SRC_Debounce ==
  EGRVlv_uRaw : Inport  Tag=mv
  DSM_bEGRVlvSSpMon : Inport  Tag=-  Port=2
  Constant : Constant  Value=EGRVlv_uSRCMax_C
  Constant1 : Constant  Value=EGRVlv_tiMaxOKDeb_C
  Constant12 : Constant  Value=EGRVlv_uSRCMin_C
  Constant2 : Constant  Value=EGRVlv_tiMaxDefDeb_C
  Constant4 : Constant  Value=EGRVlv_tiMinDefDeb_C
  Constant5 : Constant  Value=EGRVlv_tiMinOKDeb_C
  Constant6 : Constant  Value=EGRVlv_DDSens_DT  OutDataTypeStr=Inherit: Inherit via back propagation
  Constant8 : Constant  Value=EGRVlv_DDSens_DT  OutDataTypeStr=Inherit: Inherit via back propagation
  Debounce_DT : sllib/Debounce_DT
  Debounce_DT1 : sllib/Debounce_DT
  Logical Operator : Logic  Operator=OR  AllPortsSameDT=off  OutDataTypeStr=boolean
  Logical Operator11 : Logic  Operator=NOT  AllPortsSameDT=off  OutDataTypeStr=boolean
  Logical Operator12 : Logic  Operator=OR  AllPortsSameDT=off  OutDataTypeStr=boolean
  Logical Operator2 : Logic  Operator=OR  AllPortsSameDT=off  OutDataTypeStr=boolean
  Logical Operator{3..5,7,31} (5 alike) : Logic  AllPortsSameDT=off  OutDataTypeStr=boolean
  Logical Operator30 : Logic  Operator=NOT  AllPortsSameDT=off  OutDataTypeStr=boolean
  Relational Operator : RelationalOperator  Operator=>  OutDataTypeStr=boolean  RndMeth=Nearest  InputSameDT=on
  Relational Operator1 : RelationalOperator  Operator=<  OutDataTypeStr=boolean  RndMeth=Nearest  InputSameDT=on
  EGRVlv_bSRCMaxDeb_DSM : Outport  Tag=-
  EGRVlv_bFinalDef : Outport  Tag=-  Port=2
  EGRVlv_bSRCMinDeb_DSM : Outport  Tag=-  Port=3
  EGRVlv_bProvDef : Outport  Tag=-  Port=4
  wires:
  Relational Operator1/1 -> Logical Operator4/1
  [stSigPathDef] -> Logical Operator4/2
  [stSigPathDef] -> Logical Operator5/2
  [stSigPathDef] -> Logical Operator7/1
  EGRVlv_uRaw/1 -> Relational Operator1/1, Relational Operator/1
  Logical Operator12/1 -> Logical Operator30/1, EGRVlv_bFinalDef/1
  Logical Operator30/1 -> Logical Operator31/1
  Logical Operator31/1 -> EGRVlv_bProvDef/1
  Logical Operator/1 -> Logical Operator12/1
  [stSigPathDef] -> Logical Operator11/1
  Logical Operator11/1 -> Logical Operator12/2
  Debounce_DT/1 -> Logical Operator5/1
  Constant4/1 -> Debounce_DT1/2
  Constant1/1 -> Debounce_DT/3
  Constant2/1 -> Debounce_DT/2
  Constant5/1 -> Debounce_DT1/3
  Constant6/1 -> Debounce_DT/4
  Constant8/1 -> Debounce_DT1/4
  Constant/1 -> Relational Operator/2
  Logical Operator3/1 -> Debounce_DT/1, [bSRCMax]  "EGRVlv_bSRCMax"
  Constant12/1 -> Relational Operator1/2
  Logical Operator4/1 -> Debounce_DT1/1, [bSRCMin]  "EGRVlv_bSRCMin"
  Logical Operator5/1 -> EGRVlv_bSRCMaxDeb_DSM/1, Logical Operator/1
  Logical Operator7/1 -> EGRVlv_bSRCMinDeb_DSM/1, Logical Operator/2
  [bSRCMax] -> Logical Operator2/1
  [bSRCMin] -> Logical Operator2/2
  DSM_bEGRVlvSSpMon/1 -> [stSigPathDef]
  Relational Operator/1 -> Logical Operator3/1
  [stSigPathDef] -> Logical Operator3/2
  Logical Operator2/1 -> Logical Operator31/2
  Debounce_DT1/1 -> Logical Operator7/2

== system EGRVlv_DDSens/Overview/EGRVlv_DDSens/U2R_Cnv ==
  EGRVlv_uRaw : Inport  Tag=mv
  EGRVlv_rTransf_CUR : Lookup_n-D  DialogController=Simulink.DDGSource  NumberOfTableDimensions=1  BreakpointsForDimension1=EGRVlv_rTransf_CURX  BreakpointsForDimension2=CEngDsT_tTransf_CURX  IndexSearchMethod=Linear search  BeginIndexSearchUsingPreviousIndexResult=on  Table=EGRVlv_rTransf_CUR  TableDataTypeStr=Inherit: Inherit from 'Table data'  ExtrapMethod=Clip  UseLastTableValue=on  InternalRulePriority=Speed  OutDataTypeStr=Inherit: Inherit from 'Table data'  SaturateOnIntegerOverflow=on
  EGRVlv_rSens : Outport  Tag=%
  wires:
  EGRVlv_rTransf_CUR/1 -> EGRVlv_rSens/1
  EGRVlv_uRaw/1 -> EGRVlv_rTransf_CUR/1
